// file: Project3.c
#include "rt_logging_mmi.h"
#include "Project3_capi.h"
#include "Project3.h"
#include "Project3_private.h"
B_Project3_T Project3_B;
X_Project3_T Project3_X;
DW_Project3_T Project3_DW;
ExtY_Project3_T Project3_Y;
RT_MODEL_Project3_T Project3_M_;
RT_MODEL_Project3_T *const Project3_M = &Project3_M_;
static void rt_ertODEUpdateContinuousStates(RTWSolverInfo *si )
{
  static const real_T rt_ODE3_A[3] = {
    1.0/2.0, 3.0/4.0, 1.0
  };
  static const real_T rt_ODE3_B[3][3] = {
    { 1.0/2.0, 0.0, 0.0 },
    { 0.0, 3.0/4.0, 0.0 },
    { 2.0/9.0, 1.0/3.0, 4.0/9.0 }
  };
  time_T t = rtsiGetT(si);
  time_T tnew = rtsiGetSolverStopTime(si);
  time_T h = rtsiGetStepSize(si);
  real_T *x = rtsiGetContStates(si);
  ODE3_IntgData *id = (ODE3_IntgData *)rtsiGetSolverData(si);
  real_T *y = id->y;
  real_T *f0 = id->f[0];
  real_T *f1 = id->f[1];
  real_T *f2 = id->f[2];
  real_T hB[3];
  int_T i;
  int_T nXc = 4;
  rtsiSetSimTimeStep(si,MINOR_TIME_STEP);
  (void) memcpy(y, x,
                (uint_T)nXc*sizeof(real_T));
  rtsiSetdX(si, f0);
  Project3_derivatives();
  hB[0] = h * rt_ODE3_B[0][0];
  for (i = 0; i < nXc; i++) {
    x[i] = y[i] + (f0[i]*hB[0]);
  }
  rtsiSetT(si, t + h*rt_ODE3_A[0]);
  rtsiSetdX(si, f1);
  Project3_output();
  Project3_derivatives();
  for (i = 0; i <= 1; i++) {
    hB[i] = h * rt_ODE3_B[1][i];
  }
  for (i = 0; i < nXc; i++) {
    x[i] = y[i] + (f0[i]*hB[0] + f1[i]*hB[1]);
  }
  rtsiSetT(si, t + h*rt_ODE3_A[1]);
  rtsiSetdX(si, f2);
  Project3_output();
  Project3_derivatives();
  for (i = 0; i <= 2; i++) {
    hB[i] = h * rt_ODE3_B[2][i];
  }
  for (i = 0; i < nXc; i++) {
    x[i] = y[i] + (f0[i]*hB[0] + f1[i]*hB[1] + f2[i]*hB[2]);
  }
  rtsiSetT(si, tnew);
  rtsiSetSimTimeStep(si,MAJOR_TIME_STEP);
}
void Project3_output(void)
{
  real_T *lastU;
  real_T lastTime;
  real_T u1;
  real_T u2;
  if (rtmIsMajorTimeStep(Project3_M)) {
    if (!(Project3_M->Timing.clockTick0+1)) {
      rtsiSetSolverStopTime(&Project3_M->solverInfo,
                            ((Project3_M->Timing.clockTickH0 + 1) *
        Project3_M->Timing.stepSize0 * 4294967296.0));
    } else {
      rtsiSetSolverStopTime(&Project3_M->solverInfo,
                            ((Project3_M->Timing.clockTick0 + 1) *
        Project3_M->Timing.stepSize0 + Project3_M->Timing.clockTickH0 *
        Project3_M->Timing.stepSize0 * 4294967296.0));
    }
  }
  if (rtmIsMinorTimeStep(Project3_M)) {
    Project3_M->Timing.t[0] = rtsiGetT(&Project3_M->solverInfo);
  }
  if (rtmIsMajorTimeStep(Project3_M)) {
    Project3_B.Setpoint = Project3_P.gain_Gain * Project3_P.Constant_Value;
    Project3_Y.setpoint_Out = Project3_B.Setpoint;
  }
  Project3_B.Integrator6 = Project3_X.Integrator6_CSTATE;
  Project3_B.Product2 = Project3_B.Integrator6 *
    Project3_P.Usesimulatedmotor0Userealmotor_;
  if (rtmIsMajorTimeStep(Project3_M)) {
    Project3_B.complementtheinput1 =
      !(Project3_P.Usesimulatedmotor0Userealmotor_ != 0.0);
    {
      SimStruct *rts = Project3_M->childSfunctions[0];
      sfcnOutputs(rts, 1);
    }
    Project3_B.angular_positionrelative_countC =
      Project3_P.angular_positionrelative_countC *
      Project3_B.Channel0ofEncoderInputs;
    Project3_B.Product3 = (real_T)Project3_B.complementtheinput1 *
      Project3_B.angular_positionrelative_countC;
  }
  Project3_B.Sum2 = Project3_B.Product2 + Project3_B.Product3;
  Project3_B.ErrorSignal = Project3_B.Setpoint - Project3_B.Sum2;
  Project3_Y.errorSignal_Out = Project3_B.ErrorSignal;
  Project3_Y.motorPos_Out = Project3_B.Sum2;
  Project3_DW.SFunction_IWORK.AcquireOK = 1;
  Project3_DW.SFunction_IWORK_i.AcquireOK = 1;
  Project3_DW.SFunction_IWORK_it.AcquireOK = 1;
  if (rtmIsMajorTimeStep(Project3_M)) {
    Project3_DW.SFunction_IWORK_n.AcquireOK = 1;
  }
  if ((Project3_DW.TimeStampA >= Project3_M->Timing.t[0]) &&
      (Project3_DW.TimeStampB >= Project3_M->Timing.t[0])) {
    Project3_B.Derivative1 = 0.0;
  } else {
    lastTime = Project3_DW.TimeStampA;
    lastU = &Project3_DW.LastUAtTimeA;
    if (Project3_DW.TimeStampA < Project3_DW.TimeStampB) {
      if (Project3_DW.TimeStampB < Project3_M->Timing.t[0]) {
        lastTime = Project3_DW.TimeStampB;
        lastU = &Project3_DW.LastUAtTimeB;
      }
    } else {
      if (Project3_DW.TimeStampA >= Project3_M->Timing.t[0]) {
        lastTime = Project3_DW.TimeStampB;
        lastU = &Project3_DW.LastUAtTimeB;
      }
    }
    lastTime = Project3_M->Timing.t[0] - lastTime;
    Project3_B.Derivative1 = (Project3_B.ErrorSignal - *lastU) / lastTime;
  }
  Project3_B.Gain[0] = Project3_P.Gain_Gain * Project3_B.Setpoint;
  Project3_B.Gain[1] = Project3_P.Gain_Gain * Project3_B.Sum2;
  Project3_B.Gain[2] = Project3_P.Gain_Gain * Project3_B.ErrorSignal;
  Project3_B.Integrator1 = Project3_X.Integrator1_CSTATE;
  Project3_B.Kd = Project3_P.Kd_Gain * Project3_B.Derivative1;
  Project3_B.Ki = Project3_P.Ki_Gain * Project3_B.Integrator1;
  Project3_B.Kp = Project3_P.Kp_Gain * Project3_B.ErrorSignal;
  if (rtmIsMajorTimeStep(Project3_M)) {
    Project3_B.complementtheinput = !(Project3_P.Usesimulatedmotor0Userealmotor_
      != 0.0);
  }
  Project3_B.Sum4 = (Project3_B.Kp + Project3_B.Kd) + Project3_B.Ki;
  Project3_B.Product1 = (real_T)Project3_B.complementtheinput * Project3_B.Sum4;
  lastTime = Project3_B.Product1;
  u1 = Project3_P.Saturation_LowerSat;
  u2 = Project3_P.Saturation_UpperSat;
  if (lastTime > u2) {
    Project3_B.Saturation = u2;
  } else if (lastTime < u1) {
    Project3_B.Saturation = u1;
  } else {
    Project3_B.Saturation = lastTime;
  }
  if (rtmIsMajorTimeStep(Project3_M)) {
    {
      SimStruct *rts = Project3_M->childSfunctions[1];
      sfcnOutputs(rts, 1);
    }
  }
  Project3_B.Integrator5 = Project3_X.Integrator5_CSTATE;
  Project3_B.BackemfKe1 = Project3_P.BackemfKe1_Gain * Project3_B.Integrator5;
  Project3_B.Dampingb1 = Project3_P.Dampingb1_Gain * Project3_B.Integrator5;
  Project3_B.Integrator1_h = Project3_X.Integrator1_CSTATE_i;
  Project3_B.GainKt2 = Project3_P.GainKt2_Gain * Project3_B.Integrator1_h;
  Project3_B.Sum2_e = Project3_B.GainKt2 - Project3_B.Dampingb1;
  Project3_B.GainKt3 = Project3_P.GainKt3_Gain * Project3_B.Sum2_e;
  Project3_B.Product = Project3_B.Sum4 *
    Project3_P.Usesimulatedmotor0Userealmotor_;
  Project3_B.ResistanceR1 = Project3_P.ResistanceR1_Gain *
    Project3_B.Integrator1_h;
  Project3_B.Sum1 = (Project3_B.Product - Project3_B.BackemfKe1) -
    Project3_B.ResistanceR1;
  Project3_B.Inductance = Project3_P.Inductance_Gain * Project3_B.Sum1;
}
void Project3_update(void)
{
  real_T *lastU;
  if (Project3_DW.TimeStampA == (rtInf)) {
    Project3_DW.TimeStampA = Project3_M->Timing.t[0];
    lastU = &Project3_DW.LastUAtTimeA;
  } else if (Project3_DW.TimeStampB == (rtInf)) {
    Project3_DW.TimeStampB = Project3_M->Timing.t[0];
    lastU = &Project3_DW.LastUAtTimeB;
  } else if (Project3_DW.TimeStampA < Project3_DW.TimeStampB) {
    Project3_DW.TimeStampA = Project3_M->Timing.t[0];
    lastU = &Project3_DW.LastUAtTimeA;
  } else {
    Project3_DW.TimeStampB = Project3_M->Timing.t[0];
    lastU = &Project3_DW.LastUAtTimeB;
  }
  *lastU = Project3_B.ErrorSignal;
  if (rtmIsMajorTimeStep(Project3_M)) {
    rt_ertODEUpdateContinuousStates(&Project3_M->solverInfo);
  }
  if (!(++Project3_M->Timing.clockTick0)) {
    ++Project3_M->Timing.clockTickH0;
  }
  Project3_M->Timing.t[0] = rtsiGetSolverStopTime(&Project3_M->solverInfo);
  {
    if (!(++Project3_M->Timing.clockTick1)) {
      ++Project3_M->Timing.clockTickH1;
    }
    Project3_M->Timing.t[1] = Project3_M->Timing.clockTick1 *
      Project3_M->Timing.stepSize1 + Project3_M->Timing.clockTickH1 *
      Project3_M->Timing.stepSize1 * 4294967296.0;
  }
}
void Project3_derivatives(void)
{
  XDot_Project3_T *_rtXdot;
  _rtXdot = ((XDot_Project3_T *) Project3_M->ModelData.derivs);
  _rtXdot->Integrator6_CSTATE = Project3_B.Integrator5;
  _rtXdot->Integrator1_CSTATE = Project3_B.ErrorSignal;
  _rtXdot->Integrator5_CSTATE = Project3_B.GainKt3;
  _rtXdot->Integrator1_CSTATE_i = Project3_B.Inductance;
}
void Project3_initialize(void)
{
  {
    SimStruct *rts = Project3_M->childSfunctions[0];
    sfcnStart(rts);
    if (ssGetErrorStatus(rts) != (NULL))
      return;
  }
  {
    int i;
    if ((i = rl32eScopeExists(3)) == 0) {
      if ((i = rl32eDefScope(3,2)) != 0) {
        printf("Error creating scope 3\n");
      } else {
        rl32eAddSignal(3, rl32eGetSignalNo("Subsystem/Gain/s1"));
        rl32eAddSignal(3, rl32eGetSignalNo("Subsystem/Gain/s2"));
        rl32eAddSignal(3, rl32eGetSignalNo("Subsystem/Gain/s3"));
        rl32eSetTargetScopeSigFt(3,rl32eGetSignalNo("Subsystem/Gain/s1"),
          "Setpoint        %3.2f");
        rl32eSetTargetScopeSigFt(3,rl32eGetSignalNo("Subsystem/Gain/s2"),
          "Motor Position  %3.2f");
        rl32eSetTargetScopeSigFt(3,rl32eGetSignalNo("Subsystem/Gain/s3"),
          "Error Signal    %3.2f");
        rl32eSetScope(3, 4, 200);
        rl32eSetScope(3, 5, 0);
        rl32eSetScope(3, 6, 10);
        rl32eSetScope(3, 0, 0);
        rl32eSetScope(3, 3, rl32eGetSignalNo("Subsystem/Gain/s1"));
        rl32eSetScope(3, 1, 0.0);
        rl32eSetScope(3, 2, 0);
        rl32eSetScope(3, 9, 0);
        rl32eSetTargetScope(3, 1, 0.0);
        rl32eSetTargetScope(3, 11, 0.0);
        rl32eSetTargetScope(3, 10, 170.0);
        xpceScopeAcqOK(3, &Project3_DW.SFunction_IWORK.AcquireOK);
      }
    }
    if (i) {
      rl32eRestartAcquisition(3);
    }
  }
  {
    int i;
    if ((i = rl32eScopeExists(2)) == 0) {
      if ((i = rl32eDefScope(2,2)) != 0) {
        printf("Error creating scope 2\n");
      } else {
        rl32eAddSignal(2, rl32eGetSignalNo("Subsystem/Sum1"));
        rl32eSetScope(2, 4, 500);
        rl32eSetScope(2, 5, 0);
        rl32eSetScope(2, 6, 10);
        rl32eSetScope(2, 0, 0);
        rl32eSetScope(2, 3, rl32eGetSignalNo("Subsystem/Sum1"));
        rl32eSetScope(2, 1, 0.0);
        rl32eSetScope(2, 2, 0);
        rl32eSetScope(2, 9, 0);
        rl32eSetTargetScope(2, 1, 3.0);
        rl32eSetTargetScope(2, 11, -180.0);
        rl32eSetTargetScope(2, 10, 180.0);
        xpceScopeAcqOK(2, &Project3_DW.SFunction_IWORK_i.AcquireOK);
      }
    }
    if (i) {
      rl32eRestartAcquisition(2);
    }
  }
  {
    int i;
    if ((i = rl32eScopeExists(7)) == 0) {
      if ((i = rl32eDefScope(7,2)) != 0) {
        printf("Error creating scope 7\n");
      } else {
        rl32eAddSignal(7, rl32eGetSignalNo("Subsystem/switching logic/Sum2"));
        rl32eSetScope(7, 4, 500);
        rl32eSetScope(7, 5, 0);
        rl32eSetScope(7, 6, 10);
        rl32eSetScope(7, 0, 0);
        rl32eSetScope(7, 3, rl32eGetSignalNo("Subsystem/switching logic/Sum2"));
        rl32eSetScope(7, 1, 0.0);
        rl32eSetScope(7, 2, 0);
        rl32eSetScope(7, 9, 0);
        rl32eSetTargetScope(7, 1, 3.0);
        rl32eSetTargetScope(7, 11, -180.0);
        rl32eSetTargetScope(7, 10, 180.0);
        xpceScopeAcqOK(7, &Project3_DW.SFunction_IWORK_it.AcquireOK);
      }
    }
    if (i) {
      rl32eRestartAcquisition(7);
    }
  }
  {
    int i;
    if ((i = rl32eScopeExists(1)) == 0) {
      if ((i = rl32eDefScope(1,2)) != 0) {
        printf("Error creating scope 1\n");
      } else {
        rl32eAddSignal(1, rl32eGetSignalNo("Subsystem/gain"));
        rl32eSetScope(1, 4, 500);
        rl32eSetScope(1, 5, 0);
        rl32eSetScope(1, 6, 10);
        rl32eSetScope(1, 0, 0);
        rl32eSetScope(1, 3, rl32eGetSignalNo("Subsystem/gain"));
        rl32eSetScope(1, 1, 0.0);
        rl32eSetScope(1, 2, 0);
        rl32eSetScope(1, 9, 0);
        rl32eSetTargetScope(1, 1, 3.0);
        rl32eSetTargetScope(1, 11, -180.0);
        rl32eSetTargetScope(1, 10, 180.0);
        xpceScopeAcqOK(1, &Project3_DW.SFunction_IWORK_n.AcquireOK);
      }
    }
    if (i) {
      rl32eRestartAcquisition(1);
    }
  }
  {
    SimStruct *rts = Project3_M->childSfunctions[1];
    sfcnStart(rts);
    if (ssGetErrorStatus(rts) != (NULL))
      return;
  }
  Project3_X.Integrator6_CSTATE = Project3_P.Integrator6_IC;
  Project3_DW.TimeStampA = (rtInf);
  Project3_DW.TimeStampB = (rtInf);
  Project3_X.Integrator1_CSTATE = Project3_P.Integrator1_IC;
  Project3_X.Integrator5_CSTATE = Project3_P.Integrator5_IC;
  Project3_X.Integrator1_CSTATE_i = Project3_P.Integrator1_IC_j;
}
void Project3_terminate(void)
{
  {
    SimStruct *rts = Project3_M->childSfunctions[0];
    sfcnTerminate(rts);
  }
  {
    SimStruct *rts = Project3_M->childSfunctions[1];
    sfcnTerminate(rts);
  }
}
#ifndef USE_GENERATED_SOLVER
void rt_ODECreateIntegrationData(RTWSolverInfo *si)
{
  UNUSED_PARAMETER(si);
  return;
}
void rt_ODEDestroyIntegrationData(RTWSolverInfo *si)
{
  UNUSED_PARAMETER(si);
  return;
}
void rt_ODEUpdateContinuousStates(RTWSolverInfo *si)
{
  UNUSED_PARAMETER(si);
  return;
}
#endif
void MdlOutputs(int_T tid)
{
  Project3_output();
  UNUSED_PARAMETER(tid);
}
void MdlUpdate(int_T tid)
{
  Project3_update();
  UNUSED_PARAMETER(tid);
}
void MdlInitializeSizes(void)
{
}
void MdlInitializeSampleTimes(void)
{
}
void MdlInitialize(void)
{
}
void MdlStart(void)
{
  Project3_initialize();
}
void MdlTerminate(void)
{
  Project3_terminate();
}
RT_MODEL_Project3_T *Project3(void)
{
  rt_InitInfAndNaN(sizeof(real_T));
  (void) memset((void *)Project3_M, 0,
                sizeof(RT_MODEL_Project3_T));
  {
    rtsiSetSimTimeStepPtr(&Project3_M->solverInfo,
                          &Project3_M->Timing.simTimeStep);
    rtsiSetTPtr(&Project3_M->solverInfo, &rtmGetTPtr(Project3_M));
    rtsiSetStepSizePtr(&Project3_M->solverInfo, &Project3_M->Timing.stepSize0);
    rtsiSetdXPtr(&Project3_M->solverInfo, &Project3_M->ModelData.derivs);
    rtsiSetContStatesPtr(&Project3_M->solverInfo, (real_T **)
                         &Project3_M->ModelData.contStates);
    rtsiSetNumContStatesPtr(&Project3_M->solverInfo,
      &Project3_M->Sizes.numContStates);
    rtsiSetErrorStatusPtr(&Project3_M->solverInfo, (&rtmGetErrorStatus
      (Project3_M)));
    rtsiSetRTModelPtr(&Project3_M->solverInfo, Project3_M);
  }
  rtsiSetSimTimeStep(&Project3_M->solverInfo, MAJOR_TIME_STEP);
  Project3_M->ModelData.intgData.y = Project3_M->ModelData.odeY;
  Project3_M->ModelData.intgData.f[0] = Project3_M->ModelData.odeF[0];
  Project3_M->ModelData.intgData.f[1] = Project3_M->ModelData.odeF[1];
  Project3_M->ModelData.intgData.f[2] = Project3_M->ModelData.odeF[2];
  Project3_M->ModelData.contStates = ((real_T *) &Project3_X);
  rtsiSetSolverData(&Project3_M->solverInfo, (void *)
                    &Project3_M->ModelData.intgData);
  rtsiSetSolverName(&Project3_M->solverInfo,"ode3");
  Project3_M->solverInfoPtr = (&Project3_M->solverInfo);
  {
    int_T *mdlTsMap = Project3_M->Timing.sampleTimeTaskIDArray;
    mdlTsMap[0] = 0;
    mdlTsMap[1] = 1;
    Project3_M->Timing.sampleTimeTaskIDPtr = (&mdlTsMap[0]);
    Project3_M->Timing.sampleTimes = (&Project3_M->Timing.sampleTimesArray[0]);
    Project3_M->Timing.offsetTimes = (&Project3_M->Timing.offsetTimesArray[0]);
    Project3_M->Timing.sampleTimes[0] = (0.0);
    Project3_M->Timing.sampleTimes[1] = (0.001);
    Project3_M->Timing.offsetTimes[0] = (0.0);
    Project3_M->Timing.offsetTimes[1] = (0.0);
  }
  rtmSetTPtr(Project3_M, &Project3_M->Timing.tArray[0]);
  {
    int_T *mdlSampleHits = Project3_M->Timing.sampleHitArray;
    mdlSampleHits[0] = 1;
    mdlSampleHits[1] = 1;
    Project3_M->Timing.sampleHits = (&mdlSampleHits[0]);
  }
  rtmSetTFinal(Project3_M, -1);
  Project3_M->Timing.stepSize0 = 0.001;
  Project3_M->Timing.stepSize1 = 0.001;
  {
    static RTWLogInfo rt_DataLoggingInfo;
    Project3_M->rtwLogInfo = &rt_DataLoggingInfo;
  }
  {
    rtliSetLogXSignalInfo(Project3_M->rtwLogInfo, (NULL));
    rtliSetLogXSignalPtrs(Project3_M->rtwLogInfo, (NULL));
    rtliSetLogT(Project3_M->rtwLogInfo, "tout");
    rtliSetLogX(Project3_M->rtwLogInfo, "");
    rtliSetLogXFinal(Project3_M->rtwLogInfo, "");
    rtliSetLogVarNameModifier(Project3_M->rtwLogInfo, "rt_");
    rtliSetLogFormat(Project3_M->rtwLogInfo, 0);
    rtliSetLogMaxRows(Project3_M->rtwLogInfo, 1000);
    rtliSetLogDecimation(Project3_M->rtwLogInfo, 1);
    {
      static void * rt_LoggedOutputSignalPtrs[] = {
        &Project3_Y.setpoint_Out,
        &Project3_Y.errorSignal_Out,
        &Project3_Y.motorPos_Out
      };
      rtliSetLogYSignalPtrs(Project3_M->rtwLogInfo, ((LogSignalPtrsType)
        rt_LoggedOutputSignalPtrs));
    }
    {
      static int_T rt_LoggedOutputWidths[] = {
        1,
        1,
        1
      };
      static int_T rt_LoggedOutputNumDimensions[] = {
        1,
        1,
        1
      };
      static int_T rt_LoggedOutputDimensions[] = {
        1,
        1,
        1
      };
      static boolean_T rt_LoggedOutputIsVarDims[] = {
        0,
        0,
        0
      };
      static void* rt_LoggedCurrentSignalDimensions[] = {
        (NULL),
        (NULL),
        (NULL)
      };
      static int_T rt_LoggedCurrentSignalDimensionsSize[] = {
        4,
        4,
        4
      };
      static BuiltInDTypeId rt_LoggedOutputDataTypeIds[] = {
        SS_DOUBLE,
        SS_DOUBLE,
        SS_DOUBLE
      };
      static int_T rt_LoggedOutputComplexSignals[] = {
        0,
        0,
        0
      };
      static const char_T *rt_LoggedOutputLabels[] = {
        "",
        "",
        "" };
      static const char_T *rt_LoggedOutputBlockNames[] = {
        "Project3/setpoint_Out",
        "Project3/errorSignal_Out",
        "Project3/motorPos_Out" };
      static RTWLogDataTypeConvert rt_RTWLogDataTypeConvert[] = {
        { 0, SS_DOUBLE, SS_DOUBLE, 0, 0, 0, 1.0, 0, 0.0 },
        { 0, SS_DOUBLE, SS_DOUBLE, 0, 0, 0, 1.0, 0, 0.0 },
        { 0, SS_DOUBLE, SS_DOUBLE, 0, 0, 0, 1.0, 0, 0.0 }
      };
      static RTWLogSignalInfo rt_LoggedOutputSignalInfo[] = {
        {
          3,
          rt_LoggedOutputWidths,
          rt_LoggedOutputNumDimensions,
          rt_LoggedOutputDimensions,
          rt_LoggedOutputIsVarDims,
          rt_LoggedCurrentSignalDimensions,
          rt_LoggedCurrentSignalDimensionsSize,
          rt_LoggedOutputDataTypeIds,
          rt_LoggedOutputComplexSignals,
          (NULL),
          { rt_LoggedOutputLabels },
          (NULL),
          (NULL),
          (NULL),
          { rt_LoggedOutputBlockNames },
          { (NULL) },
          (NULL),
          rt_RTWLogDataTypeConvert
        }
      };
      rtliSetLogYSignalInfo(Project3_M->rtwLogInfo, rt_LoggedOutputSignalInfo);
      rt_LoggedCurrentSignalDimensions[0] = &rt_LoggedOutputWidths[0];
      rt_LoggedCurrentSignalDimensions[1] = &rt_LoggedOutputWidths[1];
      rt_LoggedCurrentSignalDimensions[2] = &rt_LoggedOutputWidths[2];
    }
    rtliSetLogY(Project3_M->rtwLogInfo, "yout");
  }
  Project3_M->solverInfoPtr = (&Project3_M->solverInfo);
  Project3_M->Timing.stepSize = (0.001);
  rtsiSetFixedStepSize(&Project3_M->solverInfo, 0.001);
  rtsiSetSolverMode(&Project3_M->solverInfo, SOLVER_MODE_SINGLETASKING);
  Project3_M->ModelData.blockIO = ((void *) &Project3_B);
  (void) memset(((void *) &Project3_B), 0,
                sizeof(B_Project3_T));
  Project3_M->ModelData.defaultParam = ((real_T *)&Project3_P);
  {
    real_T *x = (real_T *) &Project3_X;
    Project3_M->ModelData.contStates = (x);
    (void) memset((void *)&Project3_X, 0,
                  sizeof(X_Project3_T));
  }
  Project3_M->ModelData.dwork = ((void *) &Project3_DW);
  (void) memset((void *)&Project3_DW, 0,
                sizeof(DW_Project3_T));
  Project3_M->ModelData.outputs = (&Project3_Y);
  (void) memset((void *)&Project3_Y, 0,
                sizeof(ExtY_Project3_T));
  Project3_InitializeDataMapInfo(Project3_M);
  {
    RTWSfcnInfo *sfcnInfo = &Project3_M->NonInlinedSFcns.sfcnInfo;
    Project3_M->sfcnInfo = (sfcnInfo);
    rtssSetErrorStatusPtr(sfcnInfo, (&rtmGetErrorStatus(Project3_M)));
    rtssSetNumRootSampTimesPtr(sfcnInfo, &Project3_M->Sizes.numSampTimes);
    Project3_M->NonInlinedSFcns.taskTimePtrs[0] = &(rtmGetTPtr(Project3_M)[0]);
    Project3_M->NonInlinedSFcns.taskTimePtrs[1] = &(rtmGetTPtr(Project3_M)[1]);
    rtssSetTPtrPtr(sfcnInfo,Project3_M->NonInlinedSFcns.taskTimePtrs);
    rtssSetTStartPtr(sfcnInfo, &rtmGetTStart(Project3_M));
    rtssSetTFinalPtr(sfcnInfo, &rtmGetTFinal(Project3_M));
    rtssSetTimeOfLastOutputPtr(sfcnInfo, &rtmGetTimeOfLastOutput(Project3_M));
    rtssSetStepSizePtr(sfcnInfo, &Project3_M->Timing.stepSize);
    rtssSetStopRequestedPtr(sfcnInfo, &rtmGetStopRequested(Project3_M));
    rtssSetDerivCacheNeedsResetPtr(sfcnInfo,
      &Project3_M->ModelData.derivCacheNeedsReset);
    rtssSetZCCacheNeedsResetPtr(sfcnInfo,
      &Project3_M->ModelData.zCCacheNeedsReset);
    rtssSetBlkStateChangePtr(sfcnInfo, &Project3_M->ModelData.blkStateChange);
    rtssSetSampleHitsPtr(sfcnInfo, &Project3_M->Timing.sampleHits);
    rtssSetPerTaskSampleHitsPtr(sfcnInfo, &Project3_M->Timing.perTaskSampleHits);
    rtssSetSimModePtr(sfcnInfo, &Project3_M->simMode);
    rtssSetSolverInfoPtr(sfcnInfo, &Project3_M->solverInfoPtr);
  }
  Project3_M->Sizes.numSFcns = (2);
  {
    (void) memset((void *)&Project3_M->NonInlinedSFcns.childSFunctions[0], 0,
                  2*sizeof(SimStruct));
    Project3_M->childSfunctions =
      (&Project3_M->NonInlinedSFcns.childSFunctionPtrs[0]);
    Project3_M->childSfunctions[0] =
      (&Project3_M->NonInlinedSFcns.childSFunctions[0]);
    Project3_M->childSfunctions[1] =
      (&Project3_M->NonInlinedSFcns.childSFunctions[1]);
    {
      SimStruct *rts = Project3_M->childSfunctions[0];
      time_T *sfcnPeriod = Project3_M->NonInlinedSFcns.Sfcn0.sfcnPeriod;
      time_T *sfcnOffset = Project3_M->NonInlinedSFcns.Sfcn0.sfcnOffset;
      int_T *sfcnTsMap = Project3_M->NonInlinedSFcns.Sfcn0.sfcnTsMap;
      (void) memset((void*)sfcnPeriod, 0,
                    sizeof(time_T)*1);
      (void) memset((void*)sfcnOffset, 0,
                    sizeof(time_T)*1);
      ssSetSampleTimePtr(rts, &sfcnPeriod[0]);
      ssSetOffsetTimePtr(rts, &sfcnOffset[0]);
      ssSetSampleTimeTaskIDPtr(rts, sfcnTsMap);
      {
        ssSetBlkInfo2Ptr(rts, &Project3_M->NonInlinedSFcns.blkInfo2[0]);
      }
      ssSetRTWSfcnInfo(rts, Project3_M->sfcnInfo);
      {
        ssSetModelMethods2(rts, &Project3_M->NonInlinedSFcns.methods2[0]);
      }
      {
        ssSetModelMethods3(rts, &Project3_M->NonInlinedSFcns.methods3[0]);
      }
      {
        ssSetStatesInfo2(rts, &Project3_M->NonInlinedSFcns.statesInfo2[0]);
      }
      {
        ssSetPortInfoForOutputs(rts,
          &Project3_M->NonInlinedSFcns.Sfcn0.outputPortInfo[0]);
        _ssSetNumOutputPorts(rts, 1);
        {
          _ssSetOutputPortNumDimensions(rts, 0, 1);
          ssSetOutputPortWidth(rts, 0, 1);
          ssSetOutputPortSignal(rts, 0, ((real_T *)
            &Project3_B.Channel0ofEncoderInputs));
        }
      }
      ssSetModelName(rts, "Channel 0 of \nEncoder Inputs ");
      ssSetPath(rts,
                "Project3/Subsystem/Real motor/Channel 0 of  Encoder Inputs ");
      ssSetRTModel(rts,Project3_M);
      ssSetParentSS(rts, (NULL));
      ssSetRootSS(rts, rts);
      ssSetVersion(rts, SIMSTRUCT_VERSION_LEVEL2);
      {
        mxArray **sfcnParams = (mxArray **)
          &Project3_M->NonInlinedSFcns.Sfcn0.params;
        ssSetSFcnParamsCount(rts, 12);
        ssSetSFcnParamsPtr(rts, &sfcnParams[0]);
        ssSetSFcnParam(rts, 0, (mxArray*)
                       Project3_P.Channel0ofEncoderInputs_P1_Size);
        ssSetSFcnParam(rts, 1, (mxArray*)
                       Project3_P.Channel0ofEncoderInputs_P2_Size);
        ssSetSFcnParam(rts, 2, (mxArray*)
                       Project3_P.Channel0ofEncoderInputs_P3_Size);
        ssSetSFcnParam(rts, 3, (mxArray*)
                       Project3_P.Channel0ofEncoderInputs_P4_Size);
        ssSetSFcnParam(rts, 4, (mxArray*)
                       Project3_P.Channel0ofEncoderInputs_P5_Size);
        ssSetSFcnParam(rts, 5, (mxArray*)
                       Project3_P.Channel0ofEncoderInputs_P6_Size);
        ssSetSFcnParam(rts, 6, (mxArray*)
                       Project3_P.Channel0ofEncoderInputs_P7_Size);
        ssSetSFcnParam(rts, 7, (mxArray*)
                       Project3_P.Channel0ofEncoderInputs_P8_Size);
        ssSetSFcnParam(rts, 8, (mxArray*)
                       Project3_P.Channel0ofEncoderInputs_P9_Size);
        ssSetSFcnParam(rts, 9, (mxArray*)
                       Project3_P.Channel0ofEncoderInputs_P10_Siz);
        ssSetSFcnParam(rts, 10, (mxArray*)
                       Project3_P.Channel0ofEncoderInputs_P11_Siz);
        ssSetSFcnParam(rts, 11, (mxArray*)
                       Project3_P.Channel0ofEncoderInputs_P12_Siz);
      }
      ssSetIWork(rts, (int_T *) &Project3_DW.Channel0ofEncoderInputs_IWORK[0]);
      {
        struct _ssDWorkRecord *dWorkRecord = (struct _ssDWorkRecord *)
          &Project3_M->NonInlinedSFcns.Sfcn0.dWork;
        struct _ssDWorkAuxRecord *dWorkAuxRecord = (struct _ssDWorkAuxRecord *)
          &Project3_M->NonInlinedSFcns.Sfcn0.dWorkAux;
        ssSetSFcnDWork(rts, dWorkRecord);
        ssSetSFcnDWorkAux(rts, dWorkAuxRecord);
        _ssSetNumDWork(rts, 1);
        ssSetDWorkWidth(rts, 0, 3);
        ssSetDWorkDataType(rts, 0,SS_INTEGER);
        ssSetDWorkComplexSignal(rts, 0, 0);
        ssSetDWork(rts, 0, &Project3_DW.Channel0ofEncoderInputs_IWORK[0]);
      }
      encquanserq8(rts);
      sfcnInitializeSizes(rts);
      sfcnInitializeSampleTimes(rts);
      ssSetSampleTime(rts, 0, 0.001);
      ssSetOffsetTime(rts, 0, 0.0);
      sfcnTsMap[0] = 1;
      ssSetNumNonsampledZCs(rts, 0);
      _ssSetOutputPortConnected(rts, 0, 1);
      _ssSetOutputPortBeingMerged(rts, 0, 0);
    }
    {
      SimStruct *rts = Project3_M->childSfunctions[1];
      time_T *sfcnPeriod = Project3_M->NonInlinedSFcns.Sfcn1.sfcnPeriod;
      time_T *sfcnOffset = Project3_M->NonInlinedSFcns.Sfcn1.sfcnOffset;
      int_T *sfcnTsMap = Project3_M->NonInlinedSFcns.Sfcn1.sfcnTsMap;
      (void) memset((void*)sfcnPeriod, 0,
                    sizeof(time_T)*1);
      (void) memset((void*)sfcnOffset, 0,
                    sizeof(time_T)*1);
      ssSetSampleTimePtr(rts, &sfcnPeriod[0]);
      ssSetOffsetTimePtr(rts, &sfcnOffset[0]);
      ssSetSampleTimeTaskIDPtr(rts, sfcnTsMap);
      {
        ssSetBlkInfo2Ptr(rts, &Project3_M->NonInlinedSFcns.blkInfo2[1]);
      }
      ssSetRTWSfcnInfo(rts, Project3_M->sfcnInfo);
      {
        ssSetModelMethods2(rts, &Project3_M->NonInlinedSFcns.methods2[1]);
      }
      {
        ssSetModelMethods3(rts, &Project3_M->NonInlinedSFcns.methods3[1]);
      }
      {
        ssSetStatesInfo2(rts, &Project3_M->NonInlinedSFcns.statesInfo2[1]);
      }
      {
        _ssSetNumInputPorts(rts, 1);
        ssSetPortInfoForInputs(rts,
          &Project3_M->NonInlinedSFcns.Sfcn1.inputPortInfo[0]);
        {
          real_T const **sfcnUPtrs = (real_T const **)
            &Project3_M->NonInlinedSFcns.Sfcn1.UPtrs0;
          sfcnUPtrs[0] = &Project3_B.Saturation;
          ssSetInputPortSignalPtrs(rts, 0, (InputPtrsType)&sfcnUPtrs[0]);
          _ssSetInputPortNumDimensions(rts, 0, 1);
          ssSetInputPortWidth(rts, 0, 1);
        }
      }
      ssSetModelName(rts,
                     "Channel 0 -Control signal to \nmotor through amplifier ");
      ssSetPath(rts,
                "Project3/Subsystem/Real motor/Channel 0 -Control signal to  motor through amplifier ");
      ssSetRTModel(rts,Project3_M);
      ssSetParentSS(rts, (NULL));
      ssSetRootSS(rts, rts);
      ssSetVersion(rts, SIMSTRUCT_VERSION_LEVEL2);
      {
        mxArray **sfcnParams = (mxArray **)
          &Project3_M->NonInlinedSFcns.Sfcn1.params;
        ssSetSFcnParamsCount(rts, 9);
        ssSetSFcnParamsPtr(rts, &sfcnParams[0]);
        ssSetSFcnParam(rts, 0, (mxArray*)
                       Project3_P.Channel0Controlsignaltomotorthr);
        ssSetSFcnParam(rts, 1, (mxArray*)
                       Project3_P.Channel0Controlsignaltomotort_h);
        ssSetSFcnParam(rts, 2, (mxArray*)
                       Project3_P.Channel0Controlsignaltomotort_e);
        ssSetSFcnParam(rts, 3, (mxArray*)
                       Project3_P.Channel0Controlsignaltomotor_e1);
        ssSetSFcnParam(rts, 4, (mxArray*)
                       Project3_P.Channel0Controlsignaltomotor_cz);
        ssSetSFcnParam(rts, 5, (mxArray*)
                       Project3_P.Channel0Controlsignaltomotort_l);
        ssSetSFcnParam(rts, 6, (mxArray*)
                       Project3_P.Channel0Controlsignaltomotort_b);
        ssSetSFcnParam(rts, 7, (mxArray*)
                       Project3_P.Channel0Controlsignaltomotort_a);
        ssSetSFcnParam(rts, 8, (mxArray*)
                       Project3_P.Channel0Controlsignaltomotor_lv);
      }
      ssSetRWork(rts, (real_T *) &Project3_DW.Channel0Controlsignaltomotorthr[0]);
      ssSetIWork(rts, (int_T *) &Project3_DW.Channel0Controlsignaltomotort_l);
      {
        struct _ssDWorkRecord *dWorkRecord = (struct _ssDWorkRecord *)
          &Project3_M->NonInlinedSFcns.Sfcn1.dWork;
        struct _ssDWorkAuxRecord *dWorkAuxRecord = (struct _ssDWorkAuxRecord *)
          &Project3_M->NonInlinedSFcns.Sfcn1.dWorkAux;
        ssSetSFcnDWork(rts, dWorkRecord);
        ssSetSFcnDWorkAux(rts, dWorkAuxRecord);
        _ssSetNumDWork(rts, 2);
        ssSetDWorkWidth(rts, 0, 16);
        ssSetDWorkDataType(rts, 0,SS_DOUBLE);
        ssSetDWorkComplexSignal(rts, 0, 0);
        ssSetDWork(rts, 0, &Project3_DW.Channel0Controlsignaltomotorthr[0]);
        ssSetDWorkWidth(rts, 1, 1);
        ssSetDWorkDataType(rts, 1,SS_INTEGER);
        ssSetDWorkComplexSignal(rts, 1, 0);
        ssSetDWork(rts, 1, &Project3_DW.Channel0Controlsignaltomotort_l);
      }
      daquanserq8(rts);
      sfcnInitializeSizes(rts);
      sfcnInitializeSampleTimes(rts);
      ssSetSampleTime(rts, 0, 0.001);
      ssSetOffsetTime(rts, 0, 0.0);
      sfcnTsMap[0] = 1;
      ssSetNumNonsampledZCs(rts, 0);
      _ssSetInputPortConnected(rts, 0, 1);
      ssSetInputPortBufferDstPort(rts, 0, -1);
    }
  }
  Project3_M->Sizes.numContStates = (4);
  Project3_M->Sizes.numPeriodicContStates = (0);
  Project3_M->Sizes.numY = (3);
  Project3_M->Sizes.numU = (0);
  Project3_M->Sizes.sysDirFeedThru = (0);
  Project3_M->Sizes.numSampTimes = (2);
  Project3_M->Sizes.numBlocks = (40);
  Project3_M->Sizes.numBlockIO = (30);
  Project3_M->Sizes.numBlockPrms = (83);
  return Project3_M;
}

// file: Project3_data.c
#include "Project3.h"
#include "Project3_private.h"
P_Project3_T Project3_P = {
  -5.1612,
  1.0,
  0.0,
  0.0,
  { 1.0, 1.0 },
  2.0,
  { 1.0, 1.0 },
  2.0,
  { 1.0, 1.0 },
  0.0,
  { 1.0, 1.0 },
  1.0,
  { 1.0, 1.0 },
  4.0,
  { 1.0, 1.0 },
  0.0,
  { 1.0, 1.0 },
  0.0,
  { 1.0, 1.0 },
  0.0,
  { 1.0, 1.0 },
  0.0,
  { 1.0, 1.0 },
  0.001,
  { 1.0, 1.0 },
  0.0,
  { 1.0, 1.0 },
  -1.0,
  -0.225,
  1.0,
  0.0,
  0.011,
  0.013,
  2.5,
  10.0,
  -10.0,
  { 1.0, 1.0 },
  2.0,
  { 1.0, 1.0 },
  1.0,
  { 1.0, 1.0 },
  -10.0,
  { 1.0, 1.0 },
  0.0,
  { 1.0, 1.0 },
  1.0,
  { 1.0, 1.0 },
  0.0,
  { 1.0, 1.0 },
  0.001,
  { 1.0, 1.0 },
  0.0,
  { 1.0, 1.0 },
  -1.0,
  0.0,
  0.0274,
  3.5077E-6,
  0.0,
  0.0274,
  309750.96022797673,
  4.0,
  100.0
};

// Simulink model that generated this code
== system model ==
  setpoint_Out : Outport  <- 1: gain
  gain : Gain  <- 1: Constant
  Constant : Constant  Value=-5.1612
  errorSignal_Out : Outport  <- 1: Sum1
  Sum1 : Sum  Inputs=+-  <- 1: gain, 2: Sum2
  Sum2 : Sum  Inputs=++  <- 1: Product2, 2: Product3
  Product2 : Product  <- 1: Integrator6, 2: Constant#1
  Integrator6 : Integrator  <- 1: Integrator5
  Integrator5 : Integrator  <- 1: GainKt3
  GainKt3 : Gain  Gain=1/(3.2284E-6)  <- 1: Sum#1
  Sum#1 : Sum  Inputs=+-  <- 1: GainKt2, 2: Dampingb1
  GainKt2 : Gain  Gain=0.0274  <- 1: Integrator1
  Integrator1 : Integrator  <- 1: Inductance
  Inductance : Gain  Gain=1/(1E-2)  <- 1: Sum#2
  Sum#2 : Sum  Inputs=+--  <- 1: Product, 2: BackemfKe1, 3: ResistanceR1
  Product : Product  <- 1: Sum4, 2: Constant#1
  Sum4 : Sum  Inputs=+++  <- 1: Kp, 2: Kd, 3: Ki
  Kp : Gain  Gain=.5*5  <- 1: Sum1
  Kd : Gain  Gain=.011  <- 1: Derivative1
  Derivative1 : Derivative  <- 1: Sum1
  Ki : Gain  Gain=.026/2  <- 1: Integrator#1
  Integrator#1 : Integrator  <- 1: Sum1
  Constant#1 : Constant  Value=0
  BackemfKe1 : Gain  Gain=0.0274  <- 1: Integrator5
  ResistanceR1 : Gain  Gain=4  <- 1: Integrator1
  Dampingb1 : Gain  Gain=3.5077E-6  <- 1: Integrator5
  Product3 : Product  <- 1: complementtheinput1, 2: Gain#1
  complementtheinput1 : Logic  Operator=NOT  <- 1: Constant#1
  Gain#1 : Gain  Gain=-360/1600  <- 1: Channel0ofEncoderInputs
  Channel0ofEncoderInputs : xpcquanserlib/Incremental Encoder/Q4 Enc
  motorPos_Out : Outport  <- 1: Sum2
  Gain : Gain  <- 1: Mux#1
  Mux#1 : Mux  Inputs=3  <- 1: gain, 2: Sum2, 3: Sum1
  Q4DA#1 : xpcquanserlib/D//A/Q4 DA  <- 1: Saturation
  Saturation : Saturate  UpperLimit=10  LowerLimit=-10  <- 1: Product1
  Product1 : Product  <- 1: complementtheinput, 2: Sum4
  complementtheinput : Logic  Operator=NOT  <- 1: Constant#1
